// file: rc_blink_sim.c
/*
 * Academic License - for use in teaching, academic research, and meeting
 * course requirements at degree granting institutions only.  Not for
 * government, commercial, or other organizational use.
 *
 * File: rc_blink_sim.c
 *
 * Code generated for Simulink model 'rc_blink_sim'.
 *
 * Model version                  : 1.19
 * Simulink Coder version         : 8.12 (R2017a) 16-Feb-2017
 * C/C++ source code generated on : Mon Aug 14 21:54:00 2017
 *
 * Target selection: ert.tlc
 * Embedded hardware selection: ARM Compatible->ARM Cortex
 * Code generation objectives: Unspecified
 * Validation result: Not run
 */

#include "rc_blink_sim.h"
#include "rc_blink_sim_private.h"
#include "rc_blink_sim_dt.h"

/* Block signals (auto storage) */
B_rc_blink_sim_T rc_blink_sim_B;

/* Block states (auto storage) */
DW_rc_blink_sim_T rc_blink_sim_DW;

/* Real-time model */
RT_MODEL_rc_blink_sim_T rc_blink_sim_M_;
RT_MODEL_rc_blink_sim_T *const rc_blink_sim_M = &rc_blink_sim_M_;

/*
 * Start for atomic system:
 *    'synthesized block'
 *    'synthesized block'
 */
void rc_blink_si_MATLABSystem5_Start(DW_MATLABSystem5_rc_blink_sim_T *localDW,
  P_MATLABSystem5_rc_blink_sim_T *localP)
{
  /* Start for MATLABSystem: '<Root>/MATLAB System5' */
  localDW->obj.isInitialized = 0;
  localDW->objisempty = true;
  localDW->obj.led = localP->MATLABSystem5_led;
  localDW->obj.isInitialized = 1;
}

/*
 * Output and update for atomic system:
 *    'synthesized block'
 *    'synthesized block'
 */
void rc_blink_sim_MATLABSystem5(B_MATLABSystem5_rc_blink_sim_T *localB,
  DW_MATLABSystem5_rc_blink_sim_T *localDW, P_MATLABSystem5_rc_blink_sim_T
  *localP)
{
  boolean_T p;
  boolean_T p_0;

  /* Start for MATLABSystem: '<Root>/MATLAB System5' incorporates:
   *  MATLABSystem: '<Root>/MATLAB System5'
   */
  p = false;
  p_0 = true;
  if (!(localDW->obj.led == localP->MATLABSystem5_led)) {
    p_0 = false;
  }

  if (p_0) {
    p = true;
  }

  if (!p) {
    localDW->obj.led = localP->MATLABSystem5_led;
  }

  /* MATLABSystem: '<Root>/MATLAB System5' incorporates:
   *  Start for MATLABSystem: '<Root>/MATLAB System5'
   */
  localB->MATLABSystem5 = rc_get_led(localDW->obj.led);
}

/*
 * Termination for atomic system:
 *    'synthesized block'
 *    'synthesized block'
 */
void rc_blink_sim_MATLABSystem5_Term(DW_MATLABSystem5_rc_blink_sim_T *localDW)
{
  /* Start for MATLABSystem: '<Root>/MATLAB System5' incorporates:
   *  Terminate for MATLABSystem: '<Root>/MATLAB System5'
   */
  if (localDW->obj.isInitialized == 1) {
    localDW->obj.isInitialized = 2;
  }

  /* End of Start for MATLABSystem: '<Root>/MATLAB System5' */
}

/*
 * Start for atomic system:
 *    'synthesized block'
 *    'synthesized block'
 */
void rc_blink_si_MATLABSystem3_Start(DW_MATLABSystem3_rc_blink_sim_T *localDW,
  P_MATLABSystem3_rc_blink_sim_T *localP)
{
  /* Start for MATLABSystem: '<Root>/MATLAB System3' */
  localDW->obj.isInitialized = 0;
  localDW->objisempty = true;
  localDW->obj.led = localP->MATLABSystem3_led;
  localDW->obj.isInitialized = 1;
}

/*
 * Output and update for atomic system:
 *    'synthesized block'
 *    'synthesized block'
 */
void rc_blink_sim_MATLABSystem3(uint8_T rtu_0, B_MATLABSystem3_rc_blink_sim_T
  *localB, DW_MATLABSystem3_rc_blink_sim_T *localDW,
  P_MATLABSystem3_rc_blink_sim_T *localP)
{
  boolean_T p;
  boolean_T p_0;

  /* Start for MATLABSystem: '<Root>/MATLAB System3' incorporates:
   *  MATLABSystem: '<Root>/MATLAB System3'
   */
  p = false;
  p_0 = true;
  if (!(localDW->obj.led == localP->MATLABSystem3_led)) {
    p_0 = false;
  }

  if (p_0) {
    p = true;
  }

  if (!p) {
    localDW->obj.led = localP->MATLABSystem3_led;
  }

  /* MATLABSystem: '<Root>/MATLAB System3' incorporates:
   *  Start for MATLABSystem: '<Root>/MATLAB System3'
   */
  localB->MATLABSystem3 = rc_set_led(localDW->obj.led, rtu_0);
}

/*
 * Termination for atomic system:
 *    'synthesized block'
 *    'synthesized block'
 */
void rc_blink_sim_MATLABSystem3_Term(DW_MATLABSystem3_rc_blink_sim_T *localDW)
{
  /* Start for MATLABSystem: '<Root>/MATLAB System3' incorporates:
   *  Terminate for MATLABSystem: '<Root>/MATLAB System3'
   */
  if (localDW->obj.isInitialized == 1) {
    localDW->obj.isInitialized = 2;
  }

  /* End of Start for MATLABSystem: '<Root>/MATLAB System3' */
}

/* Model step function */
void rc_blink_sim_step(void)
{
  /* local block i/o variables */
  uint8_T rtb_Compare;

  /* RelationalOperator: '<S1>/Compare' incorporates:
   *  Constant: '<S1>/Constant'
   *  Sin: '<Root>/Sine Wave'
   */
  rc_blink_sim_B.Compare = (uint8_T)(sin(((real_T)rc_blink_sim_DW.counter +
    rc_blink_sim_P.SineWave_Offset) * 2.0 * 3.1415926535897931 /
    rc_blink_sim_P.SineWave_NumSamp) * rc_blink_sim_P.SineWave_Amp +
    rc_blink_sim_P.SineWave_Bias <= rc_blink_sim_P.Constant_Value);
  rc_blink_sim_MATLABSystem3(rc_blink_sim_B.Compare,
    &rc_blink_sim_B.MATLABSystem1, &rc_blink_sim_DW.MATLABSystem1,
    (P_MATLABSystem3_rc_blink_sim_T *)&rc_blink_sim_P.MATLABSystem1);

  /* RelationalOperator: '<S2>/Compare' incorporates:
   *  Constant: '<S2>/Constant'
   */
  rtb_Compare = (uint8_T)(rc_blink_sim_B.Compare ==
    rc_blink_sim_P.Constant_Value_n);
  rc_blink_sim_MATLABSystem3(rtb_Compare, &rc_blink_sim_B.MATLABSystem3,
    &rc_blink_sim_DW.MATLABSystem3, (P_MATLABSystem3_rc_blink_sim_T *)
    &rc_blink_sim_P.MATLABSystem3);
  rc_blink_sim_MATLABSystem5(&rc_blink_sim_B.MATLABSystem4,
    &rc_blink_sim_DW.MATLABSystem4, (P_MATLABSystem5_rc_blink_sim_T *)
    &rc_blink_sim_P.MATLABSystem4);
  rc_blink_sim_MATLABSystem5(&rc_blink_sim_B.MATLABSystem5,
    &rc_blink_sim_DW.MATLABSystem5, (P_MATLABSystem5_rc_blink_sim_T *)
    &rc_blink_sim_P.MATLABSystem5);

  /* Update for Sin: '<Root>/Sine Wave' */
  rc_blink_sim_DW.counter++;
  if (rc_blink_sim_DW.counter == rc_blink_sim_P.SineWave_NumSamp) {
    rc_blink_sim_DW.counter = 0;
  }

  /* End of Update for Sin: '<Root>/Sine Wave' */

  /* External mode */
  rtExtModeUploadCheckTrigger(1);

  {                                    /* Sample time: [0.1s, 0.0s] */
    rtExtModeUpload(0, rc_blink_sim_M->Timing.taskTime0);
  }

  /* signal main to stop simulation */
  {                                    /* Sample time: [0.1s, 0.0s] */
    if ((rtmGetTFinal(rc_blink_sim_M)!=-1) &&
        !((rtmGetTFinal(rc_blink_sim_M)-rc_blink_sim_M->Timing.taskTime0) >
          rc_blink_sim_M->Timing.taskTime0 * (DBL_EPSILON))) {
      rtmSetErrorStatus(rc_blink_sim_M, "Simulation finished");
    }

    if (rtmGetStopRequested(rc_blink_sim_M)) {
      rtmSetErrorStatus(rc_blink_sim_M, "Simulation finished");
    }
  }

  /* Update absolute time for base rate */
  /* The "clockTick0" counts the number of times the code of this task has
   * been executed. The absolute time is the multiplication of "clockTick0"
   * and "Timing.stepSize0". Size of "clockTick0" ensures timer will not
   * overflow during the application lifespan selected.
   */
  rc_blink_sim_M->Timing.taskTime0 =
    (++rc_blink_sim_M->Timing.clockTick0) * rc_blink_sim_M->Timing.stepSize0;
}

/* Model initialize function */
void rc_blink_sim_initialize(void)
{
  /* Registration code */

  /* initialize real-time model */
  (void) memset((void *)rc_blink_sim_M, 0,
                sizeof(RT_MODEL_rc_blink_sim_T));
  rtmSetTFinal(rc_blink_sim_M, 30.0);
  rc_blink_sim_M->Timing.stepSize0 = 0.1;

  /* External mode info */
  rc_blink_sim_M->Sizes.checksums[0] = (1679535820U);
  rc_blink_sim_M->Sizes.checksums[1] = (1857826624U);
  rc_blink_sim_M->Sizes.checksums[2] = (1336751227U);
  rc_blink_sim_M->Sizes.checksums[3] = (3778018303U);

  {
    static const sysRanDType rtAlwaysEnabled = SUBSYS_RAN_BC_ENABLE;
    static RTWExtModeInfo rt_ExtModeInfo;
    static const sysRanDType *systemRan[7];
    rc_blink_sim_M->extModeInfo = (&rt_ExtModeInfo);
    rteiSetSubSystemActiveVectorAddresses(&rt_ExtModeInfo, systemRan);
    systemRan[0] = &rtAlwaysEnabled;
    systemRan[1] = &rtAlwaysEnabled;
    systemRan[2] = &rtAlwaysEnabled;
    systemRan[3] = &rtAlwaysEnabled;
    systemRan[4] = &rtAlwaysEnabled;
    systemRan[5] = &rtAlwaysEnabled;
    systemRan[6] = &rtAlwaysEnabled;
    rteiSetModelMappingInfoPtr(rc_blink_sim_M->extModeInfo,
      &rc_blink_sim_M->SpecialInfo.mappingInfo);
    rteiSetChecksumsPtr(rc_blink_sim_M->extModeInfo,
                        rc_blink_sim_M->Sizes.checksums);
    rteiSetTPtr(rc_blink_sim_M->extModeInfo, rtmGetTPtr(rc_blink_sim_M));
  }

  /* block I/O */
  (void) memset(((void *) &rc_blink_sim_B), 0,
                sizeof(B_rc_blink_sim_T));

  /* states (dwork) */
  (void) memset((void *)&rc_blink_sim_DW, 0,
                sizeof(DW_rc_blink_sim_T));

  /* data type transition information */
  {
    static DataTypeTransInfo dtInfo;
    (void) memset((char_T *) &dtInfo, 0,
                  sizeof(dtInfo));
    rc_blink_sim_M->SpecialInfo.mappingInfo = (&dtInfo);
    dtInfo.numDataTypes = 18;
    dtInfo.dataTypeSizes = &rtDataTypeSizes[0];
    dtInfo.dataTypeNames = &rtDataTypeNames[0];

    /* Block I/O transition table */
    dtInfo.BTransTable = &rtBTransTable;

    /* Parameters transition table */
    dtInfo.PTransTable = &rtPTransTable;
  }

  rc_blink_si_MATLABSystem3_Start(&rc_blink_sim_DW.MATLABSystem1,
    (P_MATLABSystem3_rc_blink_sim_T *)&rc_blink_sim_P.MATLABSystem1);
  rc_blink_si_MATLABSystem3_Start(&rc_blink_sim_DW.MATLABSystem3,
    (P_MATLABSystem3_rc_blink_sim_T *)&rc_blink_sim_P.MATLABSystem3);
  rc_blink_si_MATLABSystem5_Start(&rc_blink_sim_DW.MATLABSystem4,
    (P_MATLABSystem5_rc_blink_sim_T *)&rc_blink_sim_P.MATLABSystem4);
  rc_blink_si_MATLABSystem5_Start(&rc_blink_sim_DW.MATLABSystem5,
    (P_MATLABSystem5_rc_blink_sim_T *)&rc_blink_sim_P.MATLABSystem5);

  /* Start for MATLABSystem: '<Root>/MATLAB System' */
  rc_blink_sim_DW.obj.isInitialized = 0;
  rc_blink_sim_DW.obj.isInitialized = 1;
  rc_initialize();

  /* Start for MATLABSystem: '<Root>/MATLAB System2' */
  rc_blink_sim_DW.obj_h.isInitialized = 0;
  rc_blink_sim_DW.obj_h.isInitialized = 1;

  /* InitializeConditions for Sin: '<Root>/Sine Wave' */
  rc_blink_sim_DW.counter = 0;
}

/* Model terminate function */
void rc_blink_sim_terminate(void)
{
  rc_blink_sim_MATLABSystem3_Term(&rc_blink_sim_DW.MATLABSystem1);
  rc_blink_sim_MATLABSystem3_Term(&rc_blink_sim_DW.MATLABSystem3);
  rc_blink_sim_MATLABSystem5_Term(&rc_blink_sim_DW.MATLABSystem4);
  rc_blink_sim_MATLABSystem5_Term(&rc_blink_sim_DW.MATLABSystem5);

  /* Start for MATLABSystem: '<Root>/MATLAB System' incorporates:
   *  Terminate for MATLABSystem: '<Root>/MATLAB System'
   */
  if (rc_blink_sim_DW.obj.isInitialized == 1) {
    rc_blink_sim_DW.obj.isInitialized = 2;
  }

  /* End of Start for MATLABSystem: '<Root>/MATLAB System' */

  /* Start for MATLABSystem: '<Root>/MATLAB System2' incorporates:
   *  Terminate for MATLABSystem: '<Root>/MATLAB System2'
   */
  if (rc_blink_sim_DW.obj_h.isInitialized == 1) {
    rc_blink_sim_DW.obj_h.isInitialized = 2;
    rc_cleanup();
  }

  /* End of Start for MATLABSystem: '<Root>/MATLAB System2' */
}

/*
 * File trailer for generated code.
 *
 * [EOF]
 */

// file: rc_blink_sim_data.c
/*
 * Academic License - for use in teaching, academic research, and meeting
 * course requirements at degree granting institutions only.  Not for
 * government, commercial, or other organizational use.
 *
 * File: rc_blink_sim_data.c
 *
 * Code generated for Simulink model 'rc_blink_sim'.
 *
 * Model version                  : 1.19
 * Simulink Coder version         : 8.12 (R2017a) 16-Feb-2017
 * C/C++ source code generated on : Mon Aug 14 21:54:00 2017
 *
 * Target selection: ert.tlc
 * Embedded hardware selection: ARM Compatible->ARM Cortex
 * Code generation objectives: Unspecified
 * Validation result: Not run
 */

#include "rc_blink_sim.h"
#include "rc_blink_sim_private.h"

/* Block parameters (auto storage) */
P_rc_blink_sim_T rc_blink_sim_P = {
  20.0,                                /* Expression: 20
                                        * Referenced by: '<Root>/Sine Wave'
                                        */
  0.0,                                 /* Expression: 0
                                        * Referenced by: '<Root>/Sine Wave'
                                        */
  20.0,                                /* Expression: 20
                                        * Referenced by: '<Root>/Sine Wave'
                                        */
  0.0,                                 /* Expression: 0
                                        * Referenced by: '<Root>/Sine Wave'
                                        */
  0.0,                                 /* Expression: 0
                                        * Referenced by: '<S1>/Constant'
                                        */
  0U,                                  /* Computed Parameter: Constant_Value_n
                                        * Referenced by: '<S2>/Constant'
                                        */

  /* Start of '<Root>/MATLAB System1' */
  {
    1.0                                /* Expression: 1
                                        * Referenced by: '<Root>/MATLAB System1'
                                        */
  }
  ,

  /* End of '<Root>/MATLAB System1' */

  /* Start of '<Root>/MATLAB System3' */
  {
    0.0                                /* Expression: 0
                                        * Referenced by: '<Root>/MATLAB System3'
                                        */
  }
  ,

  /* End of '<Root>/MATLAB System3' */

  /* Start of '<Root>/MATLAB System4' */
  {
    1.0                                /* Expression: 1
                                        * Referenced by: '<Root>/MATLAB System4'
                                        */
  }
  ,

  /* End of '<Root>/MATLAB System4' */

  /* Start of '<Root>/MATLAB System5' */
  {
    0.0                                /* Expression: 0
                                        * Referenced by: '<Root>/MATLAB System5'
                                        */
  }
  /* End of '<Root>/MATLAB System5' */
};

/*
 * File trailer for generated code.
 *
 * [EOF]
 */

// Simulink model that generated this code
simulink model "rc_blink_sim"  (R2017a)
settings: Solver=FixedStepAuto  StartTime=0.0  StopTime=30.0  RelTol=1e-3  EnableMultiTasking=on
libraries: simulink x2

== system rc_blink_sim ==
  Compare To Zero : simulink/Logic and Bit Operations/Compare To Zero  relop=<=  OutDataTypeStr=uint8
  Compare To Zero1 : simulink/Logic and Bit Operations/Compare To Zero  relop===  OutDataTypeStr=uint8
  Input : Scope
  MATLAB System : MATLABSystem  System=rc_initialize_sys
  MATLAB System1 : MATLABSystem  System=rc_set_led_sys  led=1
  MATLAB System2 : MATLABSystem  System=rc_cleanup_sys
  MATLAB System3 : MATLABSystem  System=rc_set_led_sys  led=0
  MATLAB System4 : MATLABSystem  System=rc_get_led_sys  led=1
  MATLAB System5 : MATLABSystem  System=rc_get_led_sys  led=0
  Output : Scope  NumInputPorts=2
  Sine Wave : Sin  SineType=Sample based  Amplitude=20  Frequency=2  Samples=20  SampleTime=0.1
  get_led : Scope  NumInputPorts=2
  wires:
  Sine Wave/1 -> Compare To Zero/1
  Compare To Zero/1 -> Compare To Zero1/1, Input/1, MATLAB System1/1
  MATLAB System1/1 -> Output/1
  MATLAB System3/1 -> Output/2
  Compare To Zero1/1 -> MATLAB System3/1
  MATLAB System4/1 -> get_led/1
  MATLAB System5/1 -> get_led/2
